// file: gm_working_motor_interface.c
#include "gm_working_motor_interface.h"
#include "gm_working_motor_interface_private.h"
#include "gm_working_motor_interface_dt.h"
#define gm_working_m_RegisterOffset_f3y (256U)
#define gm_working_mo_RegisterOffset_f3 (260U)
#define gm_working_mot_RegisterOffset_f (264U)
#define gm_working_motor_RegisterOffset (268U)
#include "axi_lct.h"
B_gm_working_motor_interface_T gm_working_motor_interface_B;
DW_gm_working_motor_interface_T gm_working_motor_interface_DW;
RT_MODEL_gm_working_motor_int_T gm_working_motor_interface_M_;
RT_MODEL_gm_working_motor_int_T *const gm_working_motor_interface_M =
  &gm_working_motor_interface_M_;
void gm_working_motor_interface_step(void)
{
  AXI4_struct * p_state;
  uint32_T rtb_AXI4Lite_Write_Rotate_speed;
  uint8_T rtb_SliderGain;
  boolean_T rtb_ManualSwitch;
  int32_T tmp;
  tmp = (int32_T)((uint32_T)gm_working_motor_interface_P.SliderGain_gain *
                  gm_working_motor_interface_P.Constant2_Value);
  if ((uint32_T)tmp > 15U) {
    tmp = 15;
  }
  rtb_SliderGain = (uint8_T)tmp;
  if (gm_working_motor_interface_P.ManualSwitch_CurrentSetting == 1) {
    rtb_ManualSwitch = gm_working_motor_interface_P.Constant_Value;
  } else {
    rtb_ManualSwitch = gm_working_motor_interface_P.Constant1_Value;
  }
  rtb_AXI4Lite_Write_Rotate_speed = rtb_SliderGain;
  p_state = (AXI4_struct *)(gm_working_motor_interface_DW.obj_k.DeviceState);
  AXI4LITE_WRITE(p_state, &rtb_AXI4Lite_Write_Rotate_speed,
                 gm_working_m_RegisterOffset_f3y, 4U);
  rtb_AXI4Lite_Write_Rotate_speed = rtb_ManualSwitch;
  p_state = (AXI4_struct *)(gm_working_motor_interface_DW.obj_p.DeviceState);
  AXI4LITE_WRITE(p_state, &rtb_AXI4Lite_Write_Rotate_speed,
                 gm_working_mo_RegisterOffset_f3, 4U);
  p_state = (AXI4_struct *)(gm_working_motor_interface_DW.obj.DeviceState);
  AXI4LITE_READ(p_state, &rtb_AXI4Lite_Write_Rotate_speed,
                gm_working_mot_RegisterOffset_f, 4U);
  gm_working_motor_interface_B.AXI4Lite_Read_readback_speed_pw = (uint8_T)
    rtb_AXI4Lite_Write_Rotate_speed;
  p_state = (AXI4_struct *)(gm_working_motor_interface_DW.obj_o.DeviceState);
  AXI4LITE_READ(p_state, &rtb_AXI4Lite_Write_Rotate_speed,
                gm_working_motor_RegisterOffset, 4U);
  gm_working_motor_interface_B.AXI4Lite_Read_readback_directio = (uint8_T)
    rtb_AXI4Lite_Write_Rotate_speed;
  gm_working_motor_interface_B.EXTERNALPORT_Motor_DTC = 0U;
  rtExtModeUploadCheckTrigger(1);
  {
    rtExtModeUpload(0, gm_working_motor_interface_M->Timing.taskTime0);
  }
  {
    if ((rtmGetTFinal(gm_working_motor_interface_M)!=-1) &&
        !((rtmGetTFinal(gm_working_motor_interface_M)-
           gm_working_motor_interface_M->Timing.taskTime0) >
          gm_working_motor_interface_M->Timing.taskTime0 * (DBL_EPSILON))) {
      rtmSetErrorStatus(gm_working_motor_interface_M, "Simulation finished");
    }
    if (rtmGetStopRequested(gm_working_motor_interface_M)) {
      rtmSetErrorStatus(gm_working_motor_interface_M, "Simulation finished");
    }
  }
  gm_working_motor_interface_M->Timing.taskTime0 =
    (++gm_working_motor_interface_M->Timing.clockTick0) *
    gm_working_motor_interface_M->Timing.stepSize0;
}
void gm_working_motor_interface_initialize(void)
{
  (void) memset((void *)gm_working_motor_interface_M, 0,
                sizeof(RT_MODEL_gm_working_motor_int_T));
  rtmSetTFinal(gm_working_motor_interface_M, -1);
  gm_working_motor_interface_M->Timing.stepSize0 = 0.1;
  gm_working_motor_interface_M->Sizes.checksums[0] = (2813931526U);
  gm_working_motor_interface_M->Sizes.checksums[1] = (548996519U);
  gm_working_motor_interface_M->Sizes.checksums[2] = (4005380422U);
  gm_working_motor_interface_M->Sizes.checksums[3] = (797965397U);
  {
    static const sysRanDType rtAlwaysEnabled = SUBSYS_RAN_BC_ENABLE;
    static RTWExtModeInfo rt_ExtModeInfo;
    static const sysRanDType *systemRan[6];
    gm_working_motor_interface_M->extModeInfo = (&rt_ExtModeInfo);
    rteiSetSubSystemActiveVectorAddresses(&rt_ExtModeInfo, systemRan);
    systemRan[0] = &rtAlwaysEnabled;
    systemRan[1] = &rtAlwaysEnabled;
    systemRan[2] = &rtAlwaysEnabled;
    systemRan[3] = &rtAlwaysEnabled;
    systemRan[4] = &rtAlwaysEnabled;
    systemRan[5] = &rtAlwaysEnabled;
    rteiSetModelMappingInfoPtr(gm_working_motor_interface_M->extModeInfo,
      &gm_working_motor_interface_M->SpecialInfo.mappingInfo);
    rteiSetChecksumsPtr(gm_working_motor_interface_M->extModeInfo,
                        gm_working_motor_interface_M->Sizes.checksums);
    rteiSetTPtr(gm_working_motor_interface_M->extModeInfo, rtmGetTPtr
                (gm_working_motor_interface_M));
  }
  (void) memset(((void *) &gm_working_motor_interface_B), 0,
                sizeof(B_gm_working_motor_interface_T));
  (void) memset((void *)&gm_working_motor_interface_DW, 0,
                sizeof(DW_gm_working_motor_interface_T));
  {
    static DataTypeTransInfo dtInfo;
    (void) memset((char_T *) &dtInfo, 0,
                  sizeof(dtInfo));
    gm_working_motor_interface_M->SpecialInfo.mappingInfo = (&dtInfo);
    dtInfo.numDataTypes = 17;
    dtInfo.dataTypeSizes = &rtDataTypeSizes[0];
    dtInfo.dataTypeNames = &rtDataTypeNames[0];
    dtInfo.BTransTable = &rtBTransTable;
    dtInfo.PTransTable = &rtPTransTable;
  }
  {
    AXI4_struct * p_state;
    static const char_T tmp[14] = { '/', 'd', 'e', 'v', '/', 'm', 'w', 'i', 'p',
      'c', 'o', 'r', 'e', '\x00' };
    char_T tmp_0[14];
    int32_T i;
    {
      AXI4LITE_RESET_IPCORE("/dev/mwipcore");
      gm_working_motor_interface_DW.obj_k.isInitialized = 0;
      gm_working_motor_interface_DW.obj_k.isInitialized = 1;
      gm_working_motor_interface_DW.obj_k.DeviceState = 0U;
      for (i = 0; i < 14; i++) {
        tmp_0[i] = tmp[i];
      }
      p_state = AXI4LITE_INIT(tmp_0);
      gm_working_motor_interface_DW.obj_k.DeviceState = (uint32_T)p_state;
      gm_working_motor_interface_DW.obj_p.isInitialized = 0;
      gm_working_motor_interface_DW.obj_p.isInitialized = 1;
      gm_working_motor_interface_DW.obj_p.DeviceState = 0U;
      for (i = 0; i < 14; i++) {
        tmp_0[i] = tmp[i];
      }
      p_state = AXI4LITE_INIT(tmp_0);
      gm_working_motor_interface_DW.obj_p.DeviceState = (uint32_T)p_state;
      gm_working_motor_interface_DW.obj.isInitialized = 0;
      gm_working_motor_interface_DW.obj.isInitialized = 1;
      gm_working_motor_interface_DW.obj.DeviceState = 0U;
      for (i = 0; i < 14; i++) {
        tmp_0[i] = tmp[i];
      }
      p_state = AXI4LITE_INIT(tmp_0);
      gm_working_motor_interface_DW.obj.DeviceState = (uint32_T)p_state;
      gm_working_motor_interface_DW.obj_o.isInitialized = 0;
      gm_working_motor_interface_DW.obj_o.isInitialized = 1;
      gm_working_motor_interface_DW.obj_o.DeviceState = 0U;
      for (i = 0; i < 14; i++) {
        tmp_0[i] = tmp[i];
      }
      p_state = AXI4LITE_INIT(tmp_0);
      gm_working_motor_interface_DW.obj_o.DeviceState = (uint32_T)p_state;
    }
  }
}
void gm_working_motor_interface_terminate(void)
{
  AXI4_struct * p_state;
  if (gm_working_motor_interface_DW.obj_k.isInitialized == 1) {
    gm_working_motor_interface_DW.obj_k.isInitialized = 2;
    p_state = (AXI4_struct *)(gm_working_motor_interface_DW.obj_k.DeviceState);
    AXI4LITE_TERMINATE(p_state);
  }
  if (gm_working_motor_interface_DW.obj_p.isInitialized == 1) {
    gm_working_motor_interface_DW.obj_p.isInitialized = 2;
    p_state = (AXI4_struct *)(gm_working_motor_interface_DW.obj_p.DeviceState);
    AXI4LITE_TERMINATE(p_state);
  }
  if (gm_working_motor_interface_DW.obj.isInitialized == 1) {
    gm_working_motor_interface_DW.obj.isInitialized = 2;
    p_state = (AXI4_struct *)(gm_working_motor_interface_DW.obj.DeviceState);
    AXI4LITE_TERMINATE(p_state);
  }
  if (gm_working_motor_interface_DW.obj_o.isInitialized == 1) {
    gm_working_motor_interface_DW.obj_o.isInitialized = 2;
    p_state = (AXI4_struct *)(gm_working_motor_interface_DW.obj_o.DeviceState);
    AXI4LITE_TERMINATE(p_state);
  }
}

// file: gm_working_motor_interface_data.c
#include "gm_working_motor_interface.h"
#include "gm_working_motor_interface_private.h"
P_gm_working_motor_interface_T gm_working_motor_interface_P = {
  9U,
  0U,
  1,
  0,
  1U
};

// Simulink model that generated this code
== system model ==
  AXI4Lite_Write_Rotate_speed : axiinterfacelib/AXI4-Interface Write  <- 1: DataTypeConversion#1
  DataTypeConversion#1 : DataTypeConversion  <- 1: SliderGain
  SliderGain : simulink/Math Operations/Slider Gain  <- 1: Constant2
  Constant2 : Constant
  AXI4InterfaceWrite#1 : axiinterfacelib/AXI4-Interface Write  <- 1: DataTypeConversion#2
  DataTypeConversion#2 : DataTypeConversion  <- 1: ManualSwitch
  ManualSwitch : ManualSwitch  <- 1: Constant, 2: Constant1
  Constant : Constant
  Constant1 : Constant  Value=0
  DataTypeConversion#3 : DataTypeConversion  <- 1: AXI4InterfaceRead#1
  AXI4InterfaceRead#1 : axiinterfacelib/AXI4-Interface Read
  DataTypeConversion#4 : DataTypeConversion  <- 1: AXI4InterfaceRead#2
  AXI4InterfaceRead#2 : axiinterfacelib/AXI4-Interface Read
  EXTERNALPORT_Motor_DTC : DataTypeConversion
